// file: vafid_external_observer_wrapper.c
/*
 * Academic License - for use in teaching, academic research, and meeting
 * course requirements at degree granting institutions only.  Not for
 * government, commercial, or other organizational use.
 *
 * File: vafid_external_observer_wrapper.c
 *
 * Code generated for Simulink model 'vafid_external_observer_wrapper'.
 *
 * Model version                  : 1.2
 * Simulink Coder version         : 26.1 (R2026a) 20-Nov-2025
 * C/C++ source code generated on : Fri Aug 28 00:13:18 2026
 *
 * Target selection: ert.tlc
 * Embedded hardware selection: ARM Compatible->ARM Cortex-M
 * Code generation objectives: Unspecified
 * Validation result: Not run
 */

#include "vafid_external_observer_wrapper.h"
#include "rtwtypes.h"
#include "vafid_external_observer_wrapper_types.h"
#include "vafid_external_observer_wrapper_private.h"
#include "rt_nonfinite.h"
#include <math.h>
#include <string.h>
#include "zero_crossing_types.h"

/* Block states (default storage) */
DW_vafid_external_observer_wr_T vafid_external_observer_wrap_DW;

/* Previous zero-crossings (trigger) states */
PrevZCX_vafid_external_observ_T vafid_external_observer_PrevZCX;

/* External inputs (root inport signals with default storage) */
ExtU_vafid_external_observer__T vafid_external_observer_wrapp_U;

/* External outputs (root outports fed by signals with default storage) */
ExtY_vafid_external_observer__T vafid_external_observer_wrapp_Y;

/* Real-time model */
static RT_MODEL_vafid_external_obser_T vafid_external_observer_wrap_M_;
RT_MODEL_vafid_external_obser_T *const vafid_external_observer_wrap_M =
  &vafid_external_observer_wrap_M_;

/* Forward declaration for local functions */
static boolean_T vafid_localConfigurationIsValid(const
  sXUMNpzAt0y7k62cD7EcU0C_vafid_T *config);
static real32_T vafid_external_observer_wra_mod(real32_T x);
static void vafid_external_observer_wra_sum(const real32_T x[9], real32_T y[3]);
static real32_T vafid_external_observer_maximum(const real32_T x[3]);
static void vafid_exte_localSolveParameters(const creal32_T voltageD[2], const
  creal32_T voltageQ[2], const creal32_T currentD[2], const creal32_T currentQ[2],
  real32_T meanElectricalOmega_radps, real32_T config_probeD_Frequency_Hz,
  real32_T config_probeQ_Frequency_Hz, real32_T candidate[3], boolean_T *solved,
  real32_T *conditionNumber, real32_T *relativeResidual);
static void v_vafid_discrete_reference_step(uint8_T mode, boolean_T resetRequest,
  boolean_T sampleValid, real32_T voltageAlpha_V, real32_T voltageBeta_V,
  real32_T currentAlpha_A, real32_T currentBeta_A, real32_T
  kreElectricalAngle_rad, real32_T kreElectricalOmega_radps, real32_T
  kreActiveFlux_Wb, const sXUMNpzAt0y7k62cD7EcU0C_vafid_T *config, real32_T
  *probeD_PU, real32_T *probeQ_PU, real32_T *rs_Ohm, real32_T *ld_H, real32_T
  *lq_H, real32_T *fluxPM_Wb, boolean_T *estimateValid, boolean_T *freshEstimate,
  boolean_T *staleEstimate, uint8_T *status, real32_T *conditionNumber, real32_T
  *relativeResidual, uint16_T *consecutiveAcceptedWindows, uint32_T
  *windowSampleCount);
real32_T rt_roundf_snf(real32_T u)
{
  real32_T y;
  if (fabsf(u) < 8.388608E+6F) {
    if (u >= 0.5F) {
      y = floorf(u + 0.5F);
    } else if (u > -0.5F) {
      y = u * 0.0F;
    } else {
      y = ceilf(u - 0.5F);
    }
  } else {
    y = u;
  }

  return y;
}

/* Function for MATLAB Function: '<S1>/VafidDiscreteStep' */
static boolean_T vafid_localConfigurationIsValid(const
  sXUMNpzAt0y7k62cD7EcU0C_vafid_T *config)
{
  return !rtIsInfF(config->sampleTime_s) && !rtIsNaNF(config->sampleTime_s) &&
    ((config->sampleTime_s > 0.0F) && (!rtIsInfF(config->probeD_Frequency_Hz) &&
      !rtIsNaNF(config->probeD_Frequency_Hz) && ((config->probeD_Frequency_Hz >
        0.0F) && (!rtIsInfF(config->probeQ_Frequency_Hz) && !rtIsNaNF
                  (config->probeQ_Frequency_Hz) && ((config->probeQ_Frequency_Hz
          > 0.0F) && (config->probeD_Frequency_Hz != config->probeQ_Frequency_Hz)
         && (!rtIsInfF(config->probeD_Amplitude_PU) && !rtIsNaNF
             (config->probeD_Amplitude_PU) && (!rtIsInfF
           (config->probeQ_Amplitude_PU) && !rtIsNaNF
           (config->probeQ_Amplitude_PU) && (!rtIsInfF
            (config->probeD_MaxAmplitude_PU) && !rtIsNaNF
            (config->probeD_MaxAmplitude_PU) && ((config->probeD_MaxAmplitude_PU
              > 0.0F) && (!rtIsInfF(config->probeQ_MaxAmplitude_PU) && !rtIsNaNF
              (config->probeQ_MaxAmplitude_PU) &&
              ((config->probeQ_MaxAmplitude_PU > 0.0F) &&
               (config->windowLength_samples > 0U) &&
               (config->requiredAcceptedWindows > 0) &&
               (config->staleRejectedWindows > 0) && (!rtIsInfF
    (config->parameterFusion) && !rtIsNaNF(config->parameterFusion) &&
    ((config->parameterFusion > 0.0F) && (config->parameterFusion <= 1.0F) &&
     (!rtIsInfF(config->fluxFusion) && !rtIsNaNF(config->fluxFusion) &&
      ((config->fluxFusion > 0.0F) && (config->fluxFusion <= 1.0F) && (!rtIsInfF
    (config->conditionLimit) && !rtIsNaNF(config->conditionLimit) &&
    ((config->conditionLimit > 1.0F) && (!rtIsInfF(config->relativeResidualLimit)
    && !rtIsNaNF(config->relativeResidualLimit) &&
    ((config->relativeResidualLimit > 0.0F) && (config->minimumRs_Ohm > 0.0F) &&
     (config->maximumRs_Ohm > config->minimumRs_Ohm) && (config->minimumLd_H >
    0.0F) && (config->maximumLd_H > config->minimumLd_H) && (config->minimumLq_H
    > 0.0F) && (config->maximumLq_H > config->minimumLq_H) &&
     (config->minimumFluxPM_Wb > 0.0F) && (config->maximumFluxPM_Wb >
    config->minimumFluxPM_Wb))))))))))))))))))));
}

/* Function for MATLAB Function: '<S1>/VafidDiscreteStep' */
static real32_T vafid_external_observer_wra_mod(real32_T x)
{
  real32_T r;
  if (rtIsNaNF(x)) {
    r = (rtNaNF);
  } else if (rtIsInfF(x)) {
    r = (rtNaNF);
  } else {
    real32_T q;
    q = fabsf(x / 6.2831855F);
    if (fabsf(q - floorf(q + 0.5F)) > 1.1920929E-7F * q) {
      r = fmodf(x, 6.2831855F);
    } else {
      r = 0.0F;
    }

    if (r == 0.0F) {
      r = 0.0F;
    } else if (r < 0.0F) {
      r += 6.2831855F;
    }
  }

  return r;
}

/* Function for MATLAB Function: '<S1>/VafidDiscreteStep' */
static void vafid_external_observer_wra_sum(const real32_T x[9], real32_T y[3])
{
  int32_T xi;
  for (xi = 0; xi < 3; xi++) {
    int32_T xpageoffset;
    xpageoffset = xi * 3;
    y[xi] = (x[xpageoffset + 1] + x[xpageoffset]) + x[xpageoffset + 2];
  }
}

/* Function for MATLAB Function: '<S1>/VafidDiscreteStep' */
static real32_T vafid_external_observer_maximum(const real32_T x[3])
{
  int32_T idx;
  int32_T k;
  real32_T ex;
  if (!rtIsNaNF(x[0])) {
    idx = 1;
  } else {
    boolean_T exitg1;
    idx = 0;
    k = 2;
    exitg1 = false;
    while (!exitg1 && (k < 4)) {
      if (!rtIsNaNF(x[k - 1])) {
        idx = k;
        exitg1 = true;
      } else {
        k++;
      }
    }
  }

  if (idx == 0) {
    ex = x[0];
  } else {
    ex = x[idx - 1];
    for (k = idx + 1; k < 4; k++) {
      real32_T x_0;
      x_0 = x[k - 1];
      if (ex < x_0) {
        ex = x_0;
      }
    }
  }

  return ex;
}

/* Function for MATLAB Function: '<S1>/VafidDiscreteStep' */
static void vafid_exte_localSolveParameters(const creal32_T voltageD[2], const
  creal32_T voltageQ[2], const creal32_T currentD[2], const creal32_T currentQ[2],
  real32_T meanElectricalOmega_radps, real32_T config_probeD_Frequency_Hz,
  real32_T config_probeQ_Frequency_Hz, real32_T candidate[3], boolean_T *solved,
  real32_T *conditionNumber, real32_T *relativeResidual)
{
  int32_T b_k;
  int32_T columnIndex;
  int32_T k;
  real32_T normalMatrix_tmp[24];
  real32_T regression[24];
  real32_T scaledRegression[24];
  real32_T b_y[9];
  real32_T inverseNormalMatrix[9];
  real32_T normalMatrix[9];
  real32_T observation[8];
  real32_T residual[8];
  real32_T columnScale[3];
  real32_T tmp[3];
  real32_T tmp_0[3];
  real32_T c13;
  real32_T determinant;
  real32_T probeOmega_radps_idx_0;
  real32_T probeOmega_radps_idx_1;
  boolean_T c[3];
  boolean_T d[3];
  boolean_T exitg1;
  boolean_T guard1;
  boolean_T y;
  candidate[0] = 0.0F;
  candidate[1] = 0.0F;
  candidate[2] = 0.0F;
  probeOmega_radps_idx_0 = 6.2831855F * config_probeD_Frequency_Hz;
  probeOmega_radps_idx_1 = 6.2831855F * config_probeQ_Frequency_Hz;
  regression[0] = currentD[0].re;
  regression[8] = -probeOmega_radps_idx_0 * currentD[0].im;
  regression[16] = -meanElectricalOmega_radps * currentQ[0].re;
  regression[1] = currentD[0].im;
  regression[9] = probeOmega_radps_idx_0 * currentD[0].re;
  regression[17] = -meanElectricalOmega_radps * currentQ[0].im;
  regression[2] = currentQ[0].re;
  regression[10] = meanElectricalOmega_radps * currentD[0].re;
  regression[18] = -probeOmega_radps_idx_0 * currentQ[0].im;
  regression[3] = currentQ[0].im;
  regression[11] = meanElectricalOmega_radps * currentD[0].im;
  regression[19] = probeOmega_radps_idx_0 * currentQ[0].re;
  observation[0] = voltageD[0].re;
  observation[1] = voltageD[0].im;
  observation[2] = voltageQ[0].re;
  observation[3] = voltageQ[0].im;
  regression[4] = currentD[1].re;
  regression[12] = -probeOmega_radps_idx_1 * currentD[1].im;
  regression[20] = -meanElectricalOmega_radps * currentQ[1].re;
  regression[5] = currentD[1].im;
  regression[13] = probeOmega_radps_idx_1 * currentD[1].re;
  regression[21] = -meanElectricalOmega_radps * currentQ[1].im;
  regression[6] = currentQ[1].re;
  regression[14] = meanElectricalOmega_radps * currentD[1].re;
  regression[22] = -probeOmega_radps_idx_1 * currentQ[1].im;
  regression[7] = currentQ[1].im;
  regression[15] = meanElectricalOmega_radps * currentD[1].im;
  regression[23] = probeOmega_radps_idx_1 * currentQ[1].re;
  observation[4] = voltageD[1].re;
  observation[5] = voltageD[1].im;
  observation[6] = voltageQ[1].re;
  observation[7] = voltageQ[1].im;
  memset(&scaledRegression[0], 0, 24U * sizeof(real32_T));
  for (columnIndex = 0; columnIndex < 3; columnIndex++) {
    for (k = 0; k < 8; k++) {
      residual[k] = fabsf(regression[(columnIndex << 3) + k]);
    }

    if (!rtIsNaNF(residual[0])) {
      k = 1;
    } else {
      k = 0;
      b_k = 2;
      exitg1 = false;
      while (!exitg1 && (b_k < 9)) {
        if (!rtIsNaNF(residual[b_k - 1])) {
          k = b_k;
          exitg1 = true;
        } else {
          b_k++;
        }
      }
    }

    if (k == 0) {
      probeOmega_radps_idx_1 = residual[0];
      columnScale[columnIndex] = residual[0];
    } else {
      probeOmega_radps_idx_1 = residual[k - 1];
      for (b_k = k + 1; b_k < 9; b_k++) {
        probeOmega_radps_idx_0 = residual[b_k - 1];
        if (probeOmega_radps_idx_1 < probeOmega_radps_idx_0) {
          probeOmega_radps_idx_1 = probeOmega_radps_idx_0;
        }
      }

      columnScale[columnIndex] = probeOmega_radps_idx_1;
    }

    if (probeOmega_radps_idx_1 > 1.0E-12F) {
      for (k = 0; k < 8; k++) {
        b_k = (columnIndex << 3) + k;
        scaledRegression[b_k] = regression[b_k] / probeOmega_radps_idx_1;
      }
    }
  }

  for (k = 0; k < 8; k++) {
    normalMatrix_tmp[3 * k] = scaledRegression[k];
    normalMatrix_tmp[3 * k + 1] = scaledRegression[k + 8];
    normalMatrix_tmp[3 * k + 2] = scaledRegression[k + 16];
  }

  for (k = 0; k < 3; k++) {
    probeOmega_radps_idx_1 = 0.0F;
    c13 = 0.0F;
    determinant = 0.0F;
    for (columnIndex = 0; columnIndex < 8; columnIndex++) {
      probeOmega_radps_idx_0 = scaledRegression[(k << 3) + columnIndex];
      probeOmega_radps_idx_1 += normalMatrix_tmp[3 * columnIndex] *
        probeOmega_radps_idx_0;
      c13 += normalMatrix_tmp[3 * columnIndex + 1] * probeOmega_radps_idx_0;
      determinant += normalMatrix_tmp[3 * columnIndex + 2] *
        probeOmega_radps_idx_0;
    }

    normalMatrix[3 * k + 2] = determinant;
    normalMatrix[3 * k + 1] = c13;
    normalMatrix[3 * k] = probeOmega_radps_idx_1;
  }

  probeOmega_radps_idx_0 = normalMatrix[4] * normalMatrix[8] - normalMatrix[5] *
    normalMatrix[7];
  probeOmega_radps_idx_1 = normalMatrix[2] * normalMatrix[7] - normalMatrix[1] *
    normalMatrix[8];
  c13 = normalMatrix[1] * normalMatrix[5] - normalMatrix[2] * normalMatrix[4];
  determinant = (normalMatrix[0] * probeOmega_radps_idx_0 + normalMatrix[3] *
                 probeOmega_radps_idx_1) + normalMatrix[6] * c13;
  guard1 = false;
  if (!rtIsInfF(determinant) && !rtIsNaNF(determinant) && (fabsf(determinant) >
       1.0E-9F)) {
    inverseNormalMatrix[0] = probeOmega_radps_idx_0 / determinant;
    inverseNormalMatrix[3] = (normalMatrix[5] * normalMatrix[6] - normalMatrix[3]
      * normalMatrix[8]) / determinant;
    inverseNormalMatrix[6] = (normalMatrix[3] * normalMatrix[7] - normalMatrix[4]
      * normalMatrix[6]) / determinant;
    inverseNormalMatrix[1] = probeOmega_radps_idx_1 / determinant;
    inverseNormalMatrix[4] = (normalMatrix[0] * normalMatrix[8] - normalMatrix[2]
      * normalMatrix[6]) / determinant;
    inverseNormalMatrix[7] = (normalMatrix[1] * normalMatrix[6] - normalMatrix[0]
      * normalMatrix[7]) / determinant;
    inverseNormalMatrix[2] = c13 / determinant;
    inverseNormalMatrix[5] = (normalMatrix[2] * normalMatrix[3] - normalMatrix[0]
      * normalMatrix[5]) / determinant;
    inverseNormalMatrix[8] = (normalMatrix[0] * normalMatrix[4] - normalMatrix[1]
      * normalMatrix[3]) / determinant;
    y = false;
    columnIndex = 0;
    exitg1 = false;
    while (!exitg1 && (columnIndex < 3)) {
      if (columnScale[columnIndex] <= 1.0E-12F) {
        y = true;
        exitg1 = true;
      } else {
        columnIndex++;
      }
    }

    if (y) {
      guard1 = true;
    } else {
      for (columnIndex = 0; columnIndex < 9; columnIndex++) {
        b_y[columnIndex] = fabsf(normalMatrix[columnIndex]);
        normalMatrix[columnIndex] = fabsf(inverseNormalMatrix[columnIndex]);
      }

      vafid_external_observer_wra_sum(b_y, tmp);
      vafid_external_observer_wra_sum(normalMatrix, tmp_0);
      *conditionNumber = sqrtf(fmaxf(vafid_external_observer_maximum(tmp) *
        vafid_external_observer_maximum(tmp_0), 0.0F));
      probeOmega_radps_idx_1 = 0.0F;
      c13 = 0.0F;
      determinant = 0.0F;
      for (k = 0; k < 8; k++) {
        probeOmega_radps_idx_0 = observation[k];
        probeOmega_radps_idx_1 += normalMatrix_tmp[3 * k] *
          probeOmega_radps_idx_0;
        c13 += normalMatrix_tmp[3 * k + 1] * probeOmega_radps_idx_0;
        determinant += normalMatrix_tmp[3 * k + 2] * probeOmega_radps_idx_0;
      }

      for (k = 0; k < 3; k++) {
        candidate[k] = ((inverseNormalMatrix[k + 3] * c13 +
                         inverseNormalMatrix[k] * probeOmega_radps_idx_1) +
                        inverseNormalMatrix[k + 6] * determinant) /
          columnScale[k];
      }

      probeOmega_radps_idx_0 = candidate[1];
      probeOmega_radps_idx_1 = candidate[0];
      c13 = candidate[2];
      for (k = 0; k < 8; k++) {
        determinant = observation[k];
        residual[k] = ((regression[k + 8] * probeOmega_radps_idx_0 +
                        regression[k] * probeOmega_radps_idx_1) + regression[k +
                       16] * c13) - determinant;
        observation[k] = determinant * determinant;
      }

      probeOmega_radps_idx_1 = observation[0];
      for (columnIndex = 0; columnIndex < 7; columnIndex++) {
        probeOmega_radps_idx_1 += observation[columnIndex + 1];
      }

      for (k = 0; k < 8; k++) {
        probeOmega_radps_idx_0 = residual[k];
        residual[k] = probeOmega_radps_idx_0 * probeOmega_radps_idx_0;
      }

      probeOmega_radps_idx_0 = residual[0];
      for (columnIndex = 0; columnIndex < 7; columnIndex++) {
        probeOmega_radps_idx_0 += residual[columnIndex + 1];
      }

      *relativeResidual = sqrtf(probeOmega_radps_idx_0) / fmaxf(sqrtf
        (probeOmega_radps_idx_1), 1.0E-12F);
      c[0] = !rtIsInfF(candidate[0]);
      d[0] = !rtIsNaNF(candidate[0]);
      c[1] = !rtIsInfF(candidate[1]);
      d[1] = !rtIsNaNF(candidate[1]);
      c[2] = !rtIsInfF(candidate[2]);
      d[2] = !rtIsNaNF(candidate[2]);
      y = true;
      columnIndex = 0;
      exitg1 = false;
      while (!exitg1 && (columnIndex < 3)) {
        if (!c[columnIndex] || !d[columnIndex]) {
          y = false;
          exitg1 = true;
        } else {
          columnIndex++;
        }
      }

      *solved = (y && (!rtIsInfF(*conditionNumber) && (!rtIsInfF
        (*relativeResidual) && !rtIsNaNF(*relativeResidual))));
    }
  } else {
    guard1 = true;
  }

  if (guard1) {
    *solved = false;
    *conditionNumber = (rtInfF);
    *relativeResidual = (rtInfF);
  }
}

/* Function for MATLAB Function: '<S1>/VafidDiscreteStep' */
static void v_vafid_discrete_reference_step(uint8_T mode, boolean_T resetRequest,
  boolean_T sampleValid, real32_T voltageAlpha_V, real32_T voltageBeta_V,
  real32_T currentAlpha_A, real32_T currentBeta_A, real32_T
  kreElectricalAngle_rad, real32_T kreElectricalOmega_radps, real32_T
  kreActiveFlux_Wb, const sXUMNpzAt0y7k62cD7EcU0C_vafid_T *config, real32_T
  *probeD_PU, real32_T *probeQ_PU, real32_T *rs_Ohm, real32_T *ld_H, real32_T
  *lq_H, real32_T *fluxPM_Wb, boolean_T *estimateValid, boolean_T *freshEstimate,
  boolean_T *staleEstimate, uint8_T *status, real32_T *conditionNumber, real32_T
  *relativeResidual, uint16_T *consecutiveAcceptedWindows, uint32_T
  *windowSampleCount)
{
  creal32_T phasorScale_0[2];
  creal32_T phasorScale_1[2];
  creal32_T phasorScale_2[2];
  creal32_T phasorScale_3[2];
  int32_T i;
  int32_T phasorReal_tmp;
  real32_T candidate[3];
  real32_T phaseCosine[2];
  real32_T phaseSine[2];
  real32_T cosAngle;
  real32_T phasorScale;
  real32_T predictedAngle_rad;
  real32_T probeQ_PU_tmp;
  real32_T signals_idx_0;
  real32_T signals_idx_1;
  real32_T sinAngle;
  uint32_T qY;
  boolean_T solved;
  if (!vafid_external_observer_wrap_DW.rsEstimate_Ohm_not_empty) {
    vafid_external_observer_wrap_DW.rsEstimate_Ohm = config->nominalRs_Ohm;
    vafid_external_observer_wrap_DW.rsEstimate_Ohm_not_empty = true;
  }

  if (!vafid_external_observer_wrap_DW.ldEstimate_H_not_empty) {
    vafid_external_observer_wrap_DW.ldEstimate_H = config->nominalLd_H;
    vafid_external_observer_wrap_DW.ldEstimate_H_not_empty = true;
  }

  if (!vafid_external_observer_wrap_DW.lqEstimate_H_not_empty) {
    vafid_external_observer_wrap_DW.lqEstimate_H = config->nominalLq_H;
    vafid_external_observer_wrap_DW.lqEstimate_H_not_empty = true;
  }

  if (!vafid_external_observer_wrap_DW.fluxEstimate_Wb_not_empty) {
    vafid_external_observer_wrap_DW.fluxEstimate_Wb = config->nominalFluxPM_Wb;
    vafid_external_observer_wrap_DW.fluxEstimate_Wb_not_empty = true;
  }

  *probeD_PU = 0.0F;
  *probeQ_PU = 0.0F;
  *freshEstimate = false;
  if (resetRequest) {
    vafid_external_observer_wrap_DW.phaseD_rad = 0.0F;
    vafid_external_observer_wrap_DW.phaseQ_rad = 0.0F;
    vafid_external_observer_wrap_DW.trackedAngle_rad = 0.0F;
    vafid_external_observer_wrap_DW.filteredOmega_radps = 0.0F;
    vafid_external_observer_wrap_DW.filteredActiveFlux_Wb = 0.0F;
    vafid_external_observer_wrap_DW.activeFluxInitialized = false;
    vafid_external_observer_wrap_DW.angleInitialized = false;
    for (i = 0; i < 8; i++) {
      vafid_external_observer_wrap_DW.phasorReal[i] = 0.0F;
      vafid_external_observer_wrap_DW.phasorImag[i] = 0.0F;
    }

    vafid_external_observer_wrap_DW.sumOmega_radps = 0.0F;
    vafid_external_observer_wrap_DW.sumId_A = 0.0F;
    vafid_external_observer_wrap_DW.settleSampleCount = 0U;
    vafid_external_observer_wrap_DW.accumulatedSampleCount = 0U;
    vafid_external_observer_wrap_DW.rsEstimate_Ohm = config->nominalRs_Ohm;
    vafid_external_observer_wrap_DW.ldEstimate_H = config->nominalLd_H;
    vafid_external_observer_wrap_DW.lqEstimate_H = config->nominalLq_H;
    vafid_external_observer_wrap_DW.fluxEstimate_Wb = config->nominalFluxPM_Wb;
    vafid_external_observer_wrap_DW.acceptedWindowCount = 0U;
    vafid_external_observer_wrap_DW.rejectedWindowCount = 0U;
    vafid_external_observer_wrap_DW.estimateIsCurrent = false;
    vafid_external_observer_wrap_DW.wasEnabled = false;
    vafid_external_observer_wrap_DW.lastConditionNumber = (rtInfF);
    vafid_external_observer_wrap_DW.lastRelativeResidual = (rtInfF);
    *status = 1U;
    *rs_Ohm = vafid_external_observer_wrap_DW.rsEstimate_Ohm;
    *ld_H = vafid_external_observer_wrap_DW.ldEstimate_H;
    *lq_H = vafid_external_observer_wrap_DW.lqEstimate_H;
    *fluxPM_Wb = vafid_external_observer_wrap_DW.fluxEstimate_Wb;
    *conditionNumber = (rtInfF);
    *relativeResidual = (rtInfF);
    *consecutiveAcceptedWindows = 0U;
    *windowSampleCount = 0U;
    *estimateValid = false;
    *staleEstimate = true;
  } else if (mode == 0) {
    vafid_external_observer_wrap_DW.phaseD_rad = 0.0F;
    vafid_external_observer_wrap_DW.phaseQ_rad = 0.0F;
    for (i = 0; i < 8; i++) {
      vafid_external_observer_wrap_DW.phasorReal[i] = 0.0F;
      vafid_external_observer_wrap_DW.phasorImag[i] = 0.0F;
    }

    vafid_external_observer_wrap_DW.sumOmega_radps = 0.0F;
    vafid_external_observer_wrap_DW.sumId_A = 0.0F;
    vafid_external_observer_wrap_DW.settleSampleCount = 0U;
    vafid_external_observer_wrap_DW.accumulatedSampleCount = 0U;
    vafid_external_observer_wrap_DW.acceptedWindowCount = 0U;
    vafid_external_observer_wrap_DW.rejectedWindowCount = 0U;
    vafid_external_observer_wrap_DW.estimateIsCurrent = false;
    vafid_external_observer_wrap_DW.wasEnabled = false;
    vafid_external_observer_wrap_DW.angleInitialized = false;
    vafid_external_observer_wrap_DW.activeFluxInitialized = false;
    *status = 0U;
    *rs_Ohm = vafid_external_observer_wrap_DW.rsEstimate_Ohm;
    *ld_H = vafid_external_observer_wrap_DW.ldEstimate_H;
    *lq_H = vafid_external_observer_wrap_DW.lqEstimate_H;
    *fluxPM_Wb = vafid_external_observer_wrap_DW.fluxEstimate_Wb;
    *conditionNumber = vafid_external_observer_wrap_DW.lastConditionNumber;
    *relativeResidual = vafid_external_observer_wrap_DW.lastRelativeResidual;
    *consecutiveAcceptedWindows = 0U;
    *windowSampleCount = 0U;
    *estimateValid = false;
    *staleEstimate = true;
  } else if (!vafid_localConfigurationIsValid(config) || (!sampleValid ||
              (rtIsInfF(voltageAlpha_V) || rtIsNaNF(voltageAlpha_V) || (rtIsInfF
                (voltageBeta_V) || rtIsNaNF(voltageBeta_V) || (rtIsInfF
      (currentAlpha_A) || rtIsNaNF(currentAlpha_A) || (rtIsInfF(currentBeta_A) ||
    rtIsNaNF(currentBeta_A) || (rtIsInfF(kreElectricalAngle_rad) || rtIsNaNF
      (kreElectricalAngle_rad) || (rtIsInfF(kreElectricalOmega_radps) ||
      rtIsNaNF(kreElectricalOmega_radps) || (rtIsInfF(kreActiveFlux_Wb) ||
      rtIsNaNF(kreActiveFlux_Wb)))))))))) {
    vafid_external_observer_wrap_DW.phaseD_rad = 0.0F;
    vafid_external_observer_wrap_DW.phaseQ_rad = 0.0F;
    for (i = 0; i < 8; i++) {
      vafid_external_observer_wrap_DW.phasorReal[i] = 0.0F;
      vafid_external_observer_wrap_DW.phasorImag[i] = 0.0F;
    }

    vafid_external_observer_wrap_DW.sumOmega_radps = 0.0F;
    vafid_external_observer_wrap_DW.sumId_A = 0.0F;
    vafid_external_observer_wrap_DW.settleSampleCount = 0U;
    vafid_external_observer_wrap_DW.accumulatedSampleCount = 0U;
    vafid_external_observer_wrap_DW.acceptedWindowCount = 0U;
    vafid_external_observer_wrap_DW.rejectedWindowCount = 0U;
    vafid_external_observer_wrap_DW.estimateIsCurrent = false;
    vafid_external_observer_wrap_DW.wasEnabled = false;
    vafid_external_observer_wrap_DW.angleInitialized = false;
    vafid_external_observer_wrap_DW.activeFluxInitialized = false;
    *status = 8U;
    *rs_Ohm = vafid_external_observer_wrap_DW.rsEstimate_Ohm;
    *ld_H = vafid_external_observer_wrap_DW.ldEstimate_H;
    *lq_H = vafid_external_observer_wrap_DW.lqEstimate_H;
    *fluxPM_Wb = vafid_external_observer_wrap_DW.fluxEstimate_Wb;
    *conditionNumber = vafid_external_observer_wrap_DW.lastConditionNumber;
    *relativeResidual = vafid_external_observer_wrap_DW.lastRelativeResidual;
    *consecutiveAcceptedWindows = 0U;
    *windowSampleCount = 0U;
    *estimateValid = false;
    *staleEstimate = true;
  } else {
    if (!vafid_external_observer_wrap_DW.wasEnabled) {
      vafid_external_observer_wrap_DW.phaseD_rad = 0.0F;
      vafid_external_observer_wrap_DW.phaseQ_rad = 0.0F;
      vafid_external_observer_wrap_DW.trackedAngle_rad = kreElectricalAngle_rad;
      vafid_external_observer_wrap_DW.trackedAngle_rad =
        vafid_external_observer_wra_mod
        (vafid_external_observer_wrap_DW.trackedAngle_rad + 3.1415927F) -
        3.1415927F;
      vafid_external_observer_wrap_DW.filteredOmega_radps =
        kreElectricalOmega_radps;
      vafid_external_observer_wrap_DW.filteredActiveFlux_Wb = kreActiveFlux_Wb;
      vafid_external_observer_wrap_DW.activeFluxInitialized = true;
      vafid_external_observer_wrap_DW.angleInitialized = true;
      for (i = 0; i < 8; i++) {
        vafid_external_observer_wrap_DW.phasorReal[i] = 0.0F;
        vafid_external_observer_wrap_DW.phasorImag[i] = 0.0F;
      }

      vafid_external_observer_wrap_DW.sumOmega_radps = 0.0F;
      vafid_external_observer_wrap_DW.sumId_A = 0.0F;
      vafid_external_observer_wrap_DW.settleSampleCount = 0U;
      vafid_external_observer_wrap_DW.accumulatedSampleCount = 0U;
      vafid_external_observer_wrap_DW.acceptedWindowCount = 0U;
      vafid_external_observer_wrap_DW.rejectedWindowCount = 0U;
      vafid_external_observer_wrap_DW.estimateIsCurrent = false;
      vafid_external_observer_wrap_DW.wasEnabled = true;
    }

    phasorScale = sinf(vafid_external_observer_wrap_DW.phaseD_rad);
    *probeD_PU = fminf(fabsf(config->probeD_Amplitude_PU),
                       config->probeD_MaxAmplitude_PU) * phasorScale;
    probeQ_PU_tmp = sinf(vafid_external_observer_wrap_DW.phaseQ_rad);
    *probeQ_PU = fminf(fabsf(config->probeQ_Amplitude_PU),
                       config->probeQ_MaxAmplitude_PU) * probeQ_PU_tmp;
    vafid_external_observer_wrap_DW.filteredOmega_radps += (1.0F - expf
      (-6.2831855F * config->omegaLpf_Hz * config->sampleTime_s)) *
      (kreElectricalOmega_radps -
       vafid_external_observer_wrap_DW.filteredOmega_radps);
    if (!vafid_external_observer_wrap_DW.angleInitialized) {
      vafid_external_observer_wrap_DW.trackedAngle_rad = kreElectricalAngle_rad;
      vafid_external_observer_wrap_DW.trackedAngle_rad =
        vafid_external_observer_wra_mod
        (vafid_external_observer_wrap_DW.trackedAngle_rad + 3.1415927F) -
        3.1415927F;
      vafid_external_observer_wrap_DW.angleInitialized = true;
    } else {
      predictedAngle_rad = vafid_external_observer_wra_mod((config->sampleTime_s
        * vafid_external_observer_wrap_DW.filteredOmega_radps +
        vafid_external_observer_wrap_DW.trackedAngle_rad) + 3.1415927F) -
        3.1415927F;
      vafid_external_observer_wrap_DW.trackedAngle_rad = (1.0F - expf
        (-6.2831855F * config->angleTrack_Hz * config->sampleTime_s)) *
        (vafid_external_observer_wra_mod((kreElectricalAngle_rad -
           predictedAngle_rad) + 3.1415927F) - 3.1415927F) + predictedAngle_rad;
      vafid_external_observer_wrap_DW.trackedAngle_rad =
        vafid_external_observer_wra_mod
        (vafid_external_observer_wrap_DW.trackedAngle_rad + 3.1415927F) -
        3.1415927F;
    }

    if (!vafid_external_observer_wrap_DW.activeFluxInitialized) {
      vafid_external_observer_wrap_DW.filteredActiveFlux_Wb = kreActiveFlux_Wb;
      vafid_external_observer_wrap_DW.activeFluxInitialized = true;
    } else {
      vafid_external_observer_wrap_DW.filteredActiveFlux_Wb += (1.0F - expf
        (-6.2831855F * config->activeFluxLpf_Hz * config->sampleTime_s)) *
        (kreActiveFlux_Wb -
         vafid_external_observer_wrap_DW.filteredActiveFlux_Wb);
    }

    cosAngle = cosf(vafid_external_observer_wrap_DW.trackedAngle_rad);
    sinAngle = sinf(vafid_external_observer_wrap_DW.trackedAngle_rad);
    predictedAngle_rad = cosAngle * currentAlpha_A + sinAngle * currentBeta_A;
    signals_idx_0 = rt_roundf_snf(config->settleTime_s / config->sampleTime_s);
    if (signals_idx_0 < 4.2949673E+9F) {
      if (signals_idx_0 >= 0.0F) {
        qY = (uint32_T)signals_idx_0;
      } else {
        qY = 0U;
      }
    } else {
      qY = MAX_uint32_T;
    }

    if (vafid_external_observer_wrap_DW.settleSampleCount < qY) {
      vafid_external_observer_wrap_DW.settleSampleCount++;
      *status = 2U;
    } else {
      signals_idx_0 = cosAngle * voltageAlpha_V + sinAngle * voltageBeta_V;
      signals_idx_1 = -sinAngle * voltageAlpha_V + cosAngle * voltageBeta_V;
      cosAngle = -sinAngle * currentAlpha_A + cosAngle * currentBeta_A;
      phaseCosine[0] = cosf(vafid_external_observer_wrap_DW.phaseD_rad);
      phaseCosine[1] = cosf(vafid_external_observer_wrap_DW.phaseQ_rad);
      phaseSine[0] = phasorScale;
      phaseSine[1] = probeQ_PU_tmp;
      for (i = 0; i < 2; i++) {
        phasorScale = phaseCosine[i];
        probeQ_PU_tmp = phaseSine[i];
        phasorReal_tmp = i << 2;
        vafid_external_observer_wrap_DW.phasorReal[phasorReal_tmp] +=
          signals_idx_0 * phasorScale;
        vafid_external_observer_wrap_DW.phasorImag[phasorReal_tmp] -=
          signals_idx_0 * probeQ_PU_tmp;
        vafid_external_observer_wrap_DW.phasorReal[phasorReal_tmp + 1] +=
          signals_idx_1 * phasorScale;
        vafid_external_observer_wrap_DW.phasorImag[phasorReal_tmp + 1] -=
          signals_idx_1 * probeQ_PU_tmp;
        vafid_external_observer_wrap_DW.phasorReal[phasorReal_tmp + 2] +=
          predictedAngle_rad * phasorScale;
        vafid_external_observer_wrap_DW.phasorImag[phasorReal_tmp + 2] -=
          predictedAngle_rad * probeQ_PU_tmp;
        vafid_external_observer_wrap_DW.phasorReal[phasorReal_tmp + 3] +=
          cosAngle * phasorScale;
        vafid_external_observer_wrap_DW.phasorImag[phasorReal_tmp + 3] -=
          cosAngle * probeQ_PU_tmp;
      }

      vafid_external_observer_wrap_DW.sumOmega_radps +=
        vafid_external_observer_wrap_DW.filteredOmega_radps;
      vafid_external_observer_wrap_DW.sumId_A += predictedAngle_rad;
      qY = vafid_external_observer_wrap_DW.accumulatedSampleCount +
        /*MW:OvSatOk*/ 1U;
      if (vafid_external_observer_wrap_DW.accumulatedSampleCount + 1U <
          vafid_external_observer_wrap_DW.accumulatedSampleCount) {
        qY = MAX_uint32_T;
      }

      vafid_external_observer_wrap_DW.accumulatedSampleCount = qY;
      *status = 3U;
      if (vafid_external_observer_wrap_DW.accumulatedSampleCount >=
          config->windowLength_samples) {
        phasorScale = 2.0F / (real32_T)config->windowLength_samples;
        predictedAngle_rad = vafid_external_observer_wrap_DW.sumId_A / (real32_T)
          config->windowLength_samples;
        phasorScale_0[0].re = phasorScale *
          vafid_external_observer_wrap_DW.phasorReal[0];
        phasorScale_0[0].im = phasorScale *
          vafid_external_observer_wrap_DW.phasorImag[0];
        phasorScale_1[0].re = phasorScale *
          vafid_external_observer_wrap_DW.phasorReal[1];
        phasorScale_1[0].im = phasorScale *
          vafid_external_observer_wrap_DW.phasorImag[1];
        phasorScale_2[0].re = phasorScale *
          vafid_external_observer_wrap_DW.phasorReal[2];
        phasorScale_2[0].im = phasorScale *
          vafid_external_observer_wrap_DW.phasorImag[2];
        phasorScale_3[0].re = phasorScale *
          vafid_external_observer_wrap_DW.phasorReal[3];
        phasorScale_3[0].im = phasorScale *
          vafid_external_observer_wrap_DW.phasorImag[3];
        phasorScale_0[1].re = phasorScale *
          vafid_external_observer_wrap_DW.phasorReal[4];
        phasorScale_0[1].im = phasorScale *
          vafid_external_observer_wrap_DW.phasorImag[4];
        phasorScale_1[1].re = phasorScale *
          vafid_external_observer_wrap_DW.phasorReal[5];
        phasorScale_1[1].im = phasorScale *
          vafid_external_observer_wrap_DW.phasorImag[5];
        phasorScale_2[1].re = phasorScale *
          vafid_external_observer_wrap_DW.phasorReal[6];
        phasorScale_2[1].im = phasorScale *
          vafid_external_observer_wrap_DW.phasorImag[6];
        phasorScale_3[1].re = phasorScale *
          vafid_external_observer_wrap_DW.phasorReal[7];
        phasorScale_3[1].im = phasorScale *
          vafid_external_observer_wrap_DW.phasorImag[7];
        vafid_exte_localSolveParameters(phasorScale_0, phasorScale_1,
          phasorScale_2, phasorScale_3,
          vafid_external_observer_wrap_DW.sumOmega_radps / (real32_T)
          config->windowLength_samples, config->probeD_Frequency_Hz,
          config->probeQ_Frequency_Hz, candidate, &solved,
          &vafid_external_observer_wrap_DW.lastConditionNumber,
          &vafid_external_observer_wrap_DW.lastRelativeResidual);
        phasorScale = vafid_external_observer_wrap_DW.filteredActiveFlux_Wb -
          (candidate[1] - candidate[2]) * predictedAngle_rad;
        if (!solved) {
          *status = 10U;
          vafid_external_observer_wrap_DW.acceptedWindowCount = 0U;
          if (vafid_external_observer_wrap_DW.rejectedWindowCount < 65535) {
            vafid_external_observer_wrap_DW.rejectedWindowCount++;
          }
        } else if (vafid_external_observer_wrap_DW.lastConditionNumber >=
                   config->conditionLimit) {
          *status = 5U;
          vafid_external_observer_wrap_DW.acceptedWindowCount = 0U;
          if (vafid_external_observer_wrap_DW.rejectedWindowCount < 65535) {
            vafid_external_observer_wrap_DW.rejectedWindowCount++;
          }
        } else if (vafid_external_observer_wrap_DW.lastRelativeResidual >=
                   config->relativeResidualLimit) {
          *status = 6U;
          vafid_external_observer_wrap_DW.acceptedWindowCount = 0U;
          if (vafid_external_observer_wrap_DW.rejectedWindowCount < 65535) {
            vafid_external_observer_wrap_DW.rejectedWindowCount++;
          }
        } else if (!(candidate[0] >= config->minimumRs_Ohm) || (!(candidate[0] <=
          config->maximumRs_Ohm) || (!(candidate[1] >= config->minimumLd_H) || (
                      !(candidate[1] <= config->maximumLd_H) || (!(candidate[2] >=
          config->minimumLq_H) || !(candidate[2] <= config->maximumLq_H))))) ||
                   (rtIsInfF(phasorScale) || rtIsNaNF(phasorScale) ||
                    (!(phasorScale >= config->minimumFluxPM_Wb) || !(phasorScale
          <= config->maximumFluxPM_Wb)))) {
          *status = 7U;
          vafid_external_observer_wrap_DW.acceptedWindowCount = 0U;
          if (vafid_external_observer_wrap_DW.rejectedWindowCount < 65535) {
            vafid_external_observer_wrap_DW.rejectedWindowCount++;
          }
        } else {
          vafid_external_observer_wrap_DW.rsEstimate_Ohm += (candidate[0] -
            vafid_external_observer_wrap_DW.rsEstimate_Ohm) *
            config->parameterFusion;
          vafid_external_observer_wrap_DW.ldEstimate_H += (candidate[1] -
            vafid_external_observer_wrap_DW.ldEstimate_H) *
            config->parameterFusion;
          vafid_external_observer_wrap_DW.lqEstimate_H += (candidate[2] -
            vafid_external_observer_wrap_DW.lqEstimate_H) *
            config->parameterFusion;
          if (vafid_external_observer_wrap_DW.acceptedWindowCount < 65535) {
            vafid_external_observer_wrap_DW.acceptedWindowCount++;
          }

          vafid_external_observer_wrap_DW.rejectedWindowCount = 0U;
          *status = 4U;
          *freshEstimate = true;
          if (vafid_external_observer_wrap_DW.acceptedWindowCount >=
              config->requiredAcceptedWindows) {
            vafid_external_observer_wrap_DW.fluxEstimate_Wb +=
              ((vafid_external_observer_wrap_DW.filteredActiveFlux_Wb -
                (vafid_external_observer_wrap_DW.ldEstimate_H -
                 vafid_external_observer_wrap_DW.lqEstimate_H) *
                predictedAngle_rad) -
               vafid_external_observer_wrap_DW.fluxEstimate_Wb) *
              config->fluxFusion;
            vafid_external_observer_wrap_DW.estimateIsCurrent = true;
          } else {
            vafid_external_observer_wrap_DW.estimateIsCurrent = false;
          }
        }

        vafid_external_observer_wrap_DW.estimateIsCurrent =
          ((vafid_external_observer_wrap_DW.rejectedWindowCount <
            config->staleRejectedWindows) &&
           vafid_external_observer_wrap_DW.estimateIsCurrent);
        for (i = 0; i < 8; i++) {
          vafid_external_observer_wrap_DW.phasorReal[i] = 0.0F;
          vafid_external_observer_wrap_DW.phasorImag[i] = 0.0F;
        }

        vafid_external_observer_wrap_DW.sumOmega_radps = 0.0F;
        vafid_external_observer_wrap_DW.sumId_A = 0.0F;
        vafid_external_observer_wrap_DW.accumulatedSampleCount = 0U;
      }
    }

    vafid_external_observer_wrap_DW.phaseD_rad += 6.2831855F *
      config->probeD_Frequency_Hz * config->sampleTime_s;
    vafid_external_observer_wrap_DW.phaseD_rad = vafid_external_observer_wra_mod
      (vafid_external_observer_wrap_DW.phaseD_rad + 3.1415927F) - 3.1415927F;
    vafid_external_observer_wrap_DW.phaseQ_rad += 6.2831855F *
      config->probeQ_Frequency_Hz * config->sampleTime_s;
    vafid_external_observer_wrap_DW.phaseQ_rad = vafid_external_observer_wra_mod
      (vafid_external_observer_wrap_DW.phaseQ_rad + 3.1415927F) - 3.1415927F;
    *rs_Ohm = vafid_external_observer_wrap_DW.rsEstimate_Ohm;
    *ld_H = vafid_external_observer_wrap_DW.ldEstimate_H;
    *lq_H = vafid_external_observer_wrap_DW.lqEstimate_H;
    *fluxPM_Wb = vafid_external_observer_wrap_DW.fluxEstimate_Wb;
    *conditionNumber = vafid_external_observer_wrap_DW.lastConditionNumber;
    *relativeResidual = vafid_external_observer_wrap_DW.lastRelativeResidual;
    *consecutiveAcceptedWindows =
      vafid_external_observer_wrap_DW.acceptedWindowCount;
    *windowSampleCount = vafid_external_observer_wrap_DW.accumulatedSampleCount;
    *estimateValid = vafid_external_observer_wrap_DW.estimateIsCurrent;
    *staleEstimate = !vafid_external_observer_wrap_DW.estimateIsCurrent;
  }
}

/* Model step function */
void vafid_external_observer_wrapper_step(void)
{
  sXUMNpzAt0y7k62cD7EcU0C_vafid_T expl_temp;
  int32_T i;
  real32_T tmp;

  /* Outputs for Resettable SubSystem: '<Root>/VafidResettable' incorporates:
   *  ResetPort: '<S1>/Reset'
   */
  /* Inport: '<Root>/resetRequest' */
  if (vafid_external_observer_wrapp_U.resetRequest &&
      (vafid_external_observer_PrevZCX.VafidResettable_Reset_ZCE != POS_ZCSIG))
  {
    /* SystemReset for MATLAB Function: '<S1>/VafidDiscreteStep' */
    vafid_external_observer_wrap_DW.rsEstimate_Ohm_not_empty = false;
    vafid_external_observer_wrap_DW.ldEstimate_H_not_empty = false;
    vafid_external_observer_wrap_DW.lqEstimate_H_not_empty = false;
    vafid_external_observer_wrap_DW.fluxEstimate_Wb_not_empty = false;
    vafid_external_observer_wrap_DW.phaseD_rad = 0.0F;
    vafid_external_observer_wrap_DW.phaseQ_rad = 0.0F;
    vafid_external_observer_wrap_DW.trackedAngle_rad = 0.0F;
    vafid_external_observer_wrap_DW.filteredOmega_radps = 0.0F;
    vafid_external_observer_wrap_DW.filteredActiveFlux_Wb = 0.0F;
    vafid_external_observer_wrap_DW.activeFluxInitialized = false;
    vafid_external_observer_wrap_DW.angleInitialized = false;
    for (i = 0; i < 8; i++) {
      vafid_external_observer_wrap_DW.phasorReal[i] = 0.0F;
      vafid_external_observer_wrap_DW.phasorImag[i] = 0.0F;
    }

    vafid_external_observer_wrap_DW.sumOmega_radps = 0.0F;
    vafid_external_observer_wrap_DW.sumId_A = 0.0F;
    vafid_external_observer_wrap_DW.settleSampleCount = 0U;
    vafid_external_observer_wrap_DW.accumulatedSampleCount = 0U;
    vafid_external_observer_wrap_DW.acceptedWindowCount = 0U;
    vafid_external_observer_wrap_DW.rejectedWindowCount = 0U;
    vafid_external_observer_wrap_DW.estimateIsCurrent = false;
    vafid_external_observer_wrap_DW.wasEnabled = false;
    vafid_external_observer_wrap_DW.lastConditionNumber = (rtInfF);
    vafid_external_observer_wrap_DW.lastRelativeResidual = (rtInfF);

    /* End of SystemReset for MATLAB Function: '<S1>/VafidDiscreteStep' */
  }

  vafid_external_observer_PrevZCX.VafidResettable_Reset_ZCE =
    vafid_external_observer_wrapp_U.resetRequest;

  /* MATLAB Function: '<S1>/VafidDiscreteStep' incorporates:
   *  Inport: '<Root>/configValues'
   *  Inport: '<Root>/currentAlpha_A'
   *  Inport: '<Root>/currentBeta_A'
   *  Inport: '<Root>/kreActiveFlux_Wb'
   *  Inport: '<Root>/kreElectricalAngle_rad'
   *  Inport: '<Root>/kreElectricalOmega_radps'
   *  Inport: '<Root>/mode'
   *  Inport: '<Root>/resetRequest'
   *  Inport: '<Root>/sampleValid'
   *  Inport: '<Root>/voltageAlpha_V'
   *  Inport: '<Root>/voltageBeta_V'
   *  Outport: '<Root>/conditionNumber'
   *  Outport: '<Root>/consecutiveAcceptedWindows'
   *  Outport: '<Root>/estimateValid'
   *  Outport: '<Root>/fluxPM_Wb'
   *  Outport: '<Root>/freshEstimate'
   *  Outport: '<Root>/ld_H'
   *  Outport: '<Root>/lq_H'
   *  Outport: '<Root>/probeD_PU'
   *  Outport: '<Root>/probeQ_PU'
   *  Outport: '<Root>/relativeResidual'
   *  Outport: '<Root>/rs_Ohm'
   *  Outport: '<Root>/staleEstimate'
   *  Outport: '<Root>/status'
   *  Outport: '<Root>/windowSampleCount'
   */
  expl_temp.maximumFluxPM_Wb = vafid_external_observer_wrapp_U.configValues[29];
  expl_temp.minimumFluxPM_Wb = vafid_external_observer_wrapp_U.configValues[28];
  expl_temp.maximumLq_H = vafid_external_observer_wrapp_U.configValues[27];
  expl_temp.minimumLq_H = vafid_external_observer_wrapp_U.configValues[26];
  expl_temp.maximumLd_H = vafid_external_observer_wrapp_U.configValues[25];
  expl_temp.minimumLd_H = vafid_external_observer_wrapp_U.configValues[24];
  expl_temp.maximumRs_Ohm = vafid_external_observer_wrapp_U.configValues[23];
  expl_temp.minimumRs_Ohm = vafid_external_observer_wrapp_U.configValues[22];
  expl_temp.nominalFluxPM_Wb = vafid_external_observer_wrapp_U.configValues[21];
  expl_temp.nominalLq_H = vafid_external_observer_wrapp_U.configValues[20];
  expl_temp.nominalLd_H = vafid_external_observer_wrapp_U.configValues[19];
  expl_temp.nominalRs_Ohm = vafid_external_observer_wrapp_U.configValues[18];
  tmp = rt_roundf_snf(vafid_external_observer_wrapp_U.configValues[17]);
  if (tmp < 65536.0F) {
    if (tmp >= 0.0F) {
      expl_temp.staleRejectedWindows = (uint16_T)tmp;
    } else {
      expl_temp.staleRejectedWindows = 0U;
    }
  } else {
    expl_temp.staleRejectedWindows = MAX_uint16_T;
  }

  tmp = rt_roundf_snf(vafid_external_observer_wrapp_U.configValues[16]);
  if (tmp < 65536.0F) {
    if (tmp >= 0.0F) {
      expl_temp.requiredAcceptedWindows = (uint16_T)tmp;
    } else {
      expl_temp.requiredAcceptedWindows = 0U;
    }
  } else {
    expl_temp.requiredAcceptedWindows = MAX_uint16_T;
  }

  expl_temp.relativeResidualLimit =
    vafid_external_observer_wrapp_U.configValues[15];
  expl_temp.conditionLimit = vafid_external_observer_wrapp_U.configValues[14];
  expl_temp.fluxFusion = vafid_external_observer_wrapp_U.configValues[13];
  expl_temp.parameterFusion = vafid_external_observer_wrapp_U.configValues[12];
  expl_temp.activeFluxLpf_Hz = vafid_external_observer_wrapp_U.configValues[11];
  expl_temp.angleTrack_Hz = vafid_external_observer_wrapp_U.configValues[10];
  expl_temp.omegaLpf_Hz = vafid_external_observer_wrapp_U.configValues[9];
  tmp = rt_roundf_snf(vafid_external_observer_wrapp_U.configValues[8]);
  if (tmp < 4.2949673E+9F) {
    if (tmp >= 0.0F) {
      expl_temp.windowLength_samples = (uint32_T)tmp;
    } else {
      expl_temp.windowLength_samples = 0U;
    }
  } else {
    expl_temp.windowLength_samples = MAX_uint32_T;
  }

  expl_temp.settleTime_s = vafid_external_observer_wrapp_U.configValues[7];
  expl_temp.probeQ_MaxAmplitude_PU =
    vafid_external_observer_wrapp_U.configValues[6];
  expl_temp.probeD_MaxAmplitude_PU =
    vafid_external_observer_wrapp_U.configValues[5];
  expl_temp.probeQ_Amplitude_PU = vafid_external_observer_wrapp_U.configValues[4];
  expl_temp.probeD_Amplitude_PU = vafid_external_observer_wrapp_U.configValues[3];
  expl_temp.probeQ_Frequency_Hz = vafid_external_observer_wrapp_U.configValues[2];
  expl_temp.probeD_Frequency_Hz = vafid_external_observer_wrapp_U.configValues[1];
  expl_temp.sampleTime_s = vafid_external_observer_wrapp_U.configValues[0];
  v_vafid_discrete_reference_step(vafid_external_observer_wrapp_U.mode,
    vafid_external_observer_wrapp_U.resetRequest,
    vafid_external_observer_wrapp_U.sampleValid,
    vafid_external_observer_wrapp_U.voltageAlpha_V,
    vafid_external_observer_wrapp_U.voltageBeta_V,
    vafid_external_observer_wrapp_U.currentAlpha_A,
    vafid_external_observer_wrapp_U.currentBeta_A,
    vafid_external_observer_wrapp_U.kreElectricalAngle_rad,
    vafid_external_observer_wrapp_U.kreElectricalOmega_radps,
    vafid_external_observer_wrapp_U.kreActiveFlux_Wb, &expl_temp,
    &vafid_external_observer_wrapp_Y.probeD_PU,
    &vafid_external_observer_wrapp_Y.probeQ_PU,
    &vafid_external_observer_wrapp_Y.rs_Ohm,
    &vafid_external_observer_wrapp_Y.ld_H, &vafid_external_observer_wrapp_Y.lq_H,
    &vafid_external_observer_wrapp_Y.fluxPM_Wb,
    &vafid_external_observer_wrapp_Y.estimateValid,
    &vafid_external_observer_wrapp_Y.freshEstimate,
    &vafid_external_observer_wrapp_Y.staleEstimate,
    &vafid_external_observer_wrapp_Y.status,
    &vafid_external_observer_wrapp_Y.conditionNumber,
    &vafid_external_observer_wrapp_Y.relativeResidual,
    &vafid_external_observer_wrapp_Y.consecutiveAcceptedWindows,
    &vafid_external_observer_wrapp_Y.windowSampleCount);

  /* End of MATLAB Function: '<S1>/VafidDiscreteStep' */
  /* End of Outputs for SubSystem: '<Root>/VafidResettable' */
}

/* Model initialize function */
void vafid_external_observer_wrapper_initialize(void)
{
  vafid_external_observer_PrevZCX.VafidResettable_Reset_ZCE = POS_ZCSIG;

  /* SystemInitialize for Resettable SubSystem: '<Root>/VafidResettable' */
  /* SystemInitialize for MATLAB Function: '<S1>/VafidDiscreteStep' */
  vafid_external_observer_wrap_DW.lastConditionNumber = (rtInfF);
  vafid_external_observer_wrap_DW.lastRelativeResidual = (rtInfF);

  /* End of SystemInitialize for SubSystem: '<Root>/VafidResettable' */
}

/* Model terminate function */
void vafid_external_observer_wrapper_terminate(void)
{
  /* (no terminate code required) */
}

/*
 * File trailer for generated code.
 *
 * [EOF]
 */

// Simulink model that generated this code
simulink model "vafid_external_observer_wrapper"  (R2026a)
settings: Solver=FixedStepDiscrete  FixedStep=5e-5

== system vafid_external_observer_wrapper ==
  mode : Inport  OutDataTypeStr=uint8  PortDimensions=1  SampleTime=5e-5
  resetRequest : Inport  Port=2  OutDataTypeStr=boolean  PortDimensions=1  SampleTime=5e-5
  sampleValid : Inport  Port=3  OutDataTypeStr=boolean  PortDimensions=1  SampleTime=5e-5
  voltageAlpha_V : Inport  Port=4  OutDataTypeStr=single  PortDimensions=1  SampleTime=5e-5
  voltageBeta_V : Inport  Port=5  OutDataTypeStr=single  PortDimensions=1  SampleTime=5e-5
  currentAlpha_A : Inport  Port=6  OutDataTypeStr=single  PortDimensions=1  SampleTime=5e-5
  currentBeta_A : Inport  Port=7  OutDataTypeStr=single  PortDimensions=1  SampleTime=5e-5
  kreElectricalAngle_rad : Inport  Port=8  OutDataTypeStr=single  PortDimensions=1  SampleTime=5e-5
  kreElectricalOmega_radps : Inport  Port=9  OutDataTypeStr=single  PortDimensions=1  SampleTime=5e-5
  kreActiveFlux_Wb : Inport  Port=10  OutDataTypeStr=single  PortDimensions=1  SampleTime=5e-5
  configValues : Inport  Port=11  OutDataTypeStr=single  PortDimensions=30  SampleTime=5e-5
  VafidResettable : Subsystem
  probeD_PU : Outport
  probeQ_PU : Outport  Port=2
  rs_Ohm : Outport  Port=3
  ld_H : Outport  Port=4
  lq_H : Outport  Port=5
  fluxPM_Wb : Outport  Port=6
  estimateValid : Outport  Port=7
  freshEstimate : Outport  Port=8
  staleEstimate : Outport  Port=9
  status : Outport  Port=10
  conditionNumber : Outport  Port=11
  relativeResidual : Outport  Port=12
  consecutiveAcceptedWindows : Outport  Port=13
  windowSampleCount : Outport  Port=14
  wires:
  VafidResettable/14(windowSampleCount) -> windowSampleCount/1
  VafidResettable/13(consecutiveAcceptedWindows) -> consecutiveAcceptedWindows/1
  VafidResettable/12(relativeResidual) -> relativeResidual/1
  VafidResettable/11(conditionNumber) -> conditionNumber/1
  VafidResettable/10(status) -> status/1
  VafidResettable/9(staleEstimate) -> staleEstimate/1
  VafidResettable/8(freshEstimate) -> freshEstimate/1
  VafidResettable/7(estimateValid) -> estimateValid/1
  VafidResettable/6(fluxPM_Wb) -> fluxPM_Wb/1
  VafidResettable/5(lq_H) -> lq_H/1
  VafidResettable/4(ld_H) -> ld_H/1
  VafidResettable/3(rs_Ohm) -> rs_Ohm/1
  VafidResettable/2(probeQ_PU) -> probeQ_PU/1
  VafidResettable/1(probeD_PU) -> probeD_PU/1
  configValues/1 -> VafidResettable/11(configValues)
  kreActiveFlux_Wb/1 -> VafidResettable/10(kreActiveFlux_Wb)
  kreElectricalOmega_radps/1 -> VafidResettable/9(kreElectricalOmega_radps)
  kreElectricalAngle_rad/1 -> VafidResettable/8(kreElectricalAngle_rad)
  currentBeta_A/1 -> VafidResettable/7(currentBeta_A)
  currentAlpha_A/1 -> VafidResettable/6(currentAlpha_A)
  voltageBeta_V/1 -> VafidResettable/5(voltageBeta_V)
  voltageAlpha_V/1 -> VafidResettable/4(voltageAlpha_V)
  sampleValid/1 -> VafidResettable/3(sampleValid)
  resetRequest/1 -> VafidResettable/2(resetRequest), VafidResettable/Reset
  mode/1 -> VafidResettable/1(mode)

== system vafid_external_observer_wrapper/VafidResettable ==
  mode : Inport
  resetRequest : Inport  Port=2
  sampleValid : Inport  Port=3
  voltageAlpha_V : Inport  Port=4
  voltageBeta_V : Inport  Port=5
  currentAlpha_A : Inport  Port=6
  currentBeta_A : Inport  Port=7
  kreElectricalAngle_rad : Inport  Port=8
  kreElectricalOmega_radps : Inport  Port=9
  kreActiveFlux_Wb : Inport  Port=10
  configValues : Inport  Port=11
  Reset : ResetPort  DisableCoverage=on
  VafidDiscreteStep : MATLAB Function  TreatAsAtomicUnit=on
  probeD_PU : Outport
  probeQ_PU : Outport  Port=2
  rs_Ohm : Outport  Port=3
  ld_H : Outport  Port=4
  lq_H : Outport  Port=5
  fluxPM_Wb : Outport  Port=6
  estimateValid : Outport  Port=7
  freshEstimate : Outport  Port=8
  staleEstimate : Outport  Port=9
  status : Outport  Port=10
  conditionNumber : Outport  Port=11
  relativeResidual : Outport  Port=12
  consecutiveAcceptedWindows : Outport  Port=13
  windowSampleCount : Outport  Port=14
  wires:
  VafidDiscreteStep/14(windowSampleCount) -> windowSampleCount/1
  VafidDiscreteStep/13(consecutiveAcceptedWindows) -> consecutiveAcceptedWindows/1
  VafidDiscreteStep/12(relativeResidual) -> relativeResidual/1
  VafidDiscreteStep/11(conditionNumber) -> conditionNumber/1
  VafidDiscreteStep/10(status) -> status/1
  VafidDiscreteStep/9(staleEstimate) -> staleEstimate/1
  VafidDiscreteStep/8(freshEstimate) -> freshEstimate/1
  VafidDiscreteStep/7(estimateValid) -> estimateValid/1
  VafidDiscreteStep/6(fluxPM_Wb) -> fluxPM_Wb/1
  VafidDiscreteStep/5(lq_H) -> lq_H/1
  VafidDiscreteStep/4(ld_H) -> ld_H/1
  VafidDiscreteStep/3(rs_Ohm) -> rs_Ohm/1
  VafidDiscreteStep/2(probeQ_PU) -> probeQ_PU/1
  VafidDiscreteStep/1(probeD_PU) -> probeD_PU/1
  configValues/1 -> VafidDiscreteStep/11(configValues)
  kreActiveFlux_Wb/1 -> VafidDiscreteStep/10(kreActiveFlux_Wb)
  kreElectricalOmega_radps/1 -> VafidDiscreteStep/9(kreElectricalOmega_radps)
  kreElectricalAngle_rad/1 -> VafidDiscreteStep/8(kreElectricalAngle_rad)
  currentBeta_A/1 -> VafidDiscreteStep/7(currentBeta_A)
  currentAlpha_A/1 -> VafidDiscreteStep/6(currentAlpha_A)
  voltageBeta_V/1 -> VafidDiscreteStep/5(voltageBeta_V)
  voltageAlpha_V/1 -> VafidDiscreteStep/4(voltageAlpha_V)
  sampleValid/1 -> VafidDiscreteStep/3(sampleValid)
  resetRequest/1 -> VafidDiscreteStep/2(resetRequest)
  mode/1 -> VafidDiscreteStep/1(mode)

== matlab function vafid_external_observer_wrapper/VafidResettable/VafidDiscreteStep ==
function [probeD_PU, probeQ_PU, rs_Ohm, ld_H, lq_H, fluxPM_Wb, estimateValid, freshEstimate, staleEstimate, status, conditionNumber, relativeResidual, consecutiveAcceptedWindows, windowSampleCount] = fcn(mode, resetRequest, sampleValid, voltageAlpha_V, voltageBeta_V, currentAlpha_A, currentBeta_A, kreElectricalAngle_rad, kreElectricalOmega_radps, kreActiveFlux_Wb, configValues)
%#codegen
[probeD_PU, probeQ_PU, rs_Ohm, ld_H, lq_H, fluxPM_Wb, estimateValid, freshEstimate, staleEstimate, status, conditionNumber, relativeResidual, consecutiveAcceptedWindows, windowSampleCount] = vafid_external_observer_wrapper_step(mode, resetRequest, sampleValid, voltageAlpha_V, voltageBeta_V, currentAlpha_A, currentBeta_A, kreElectricalAngle_rad, kreElectricalOmega_radps, kreActiveFlux_Wb, configValues);
end
